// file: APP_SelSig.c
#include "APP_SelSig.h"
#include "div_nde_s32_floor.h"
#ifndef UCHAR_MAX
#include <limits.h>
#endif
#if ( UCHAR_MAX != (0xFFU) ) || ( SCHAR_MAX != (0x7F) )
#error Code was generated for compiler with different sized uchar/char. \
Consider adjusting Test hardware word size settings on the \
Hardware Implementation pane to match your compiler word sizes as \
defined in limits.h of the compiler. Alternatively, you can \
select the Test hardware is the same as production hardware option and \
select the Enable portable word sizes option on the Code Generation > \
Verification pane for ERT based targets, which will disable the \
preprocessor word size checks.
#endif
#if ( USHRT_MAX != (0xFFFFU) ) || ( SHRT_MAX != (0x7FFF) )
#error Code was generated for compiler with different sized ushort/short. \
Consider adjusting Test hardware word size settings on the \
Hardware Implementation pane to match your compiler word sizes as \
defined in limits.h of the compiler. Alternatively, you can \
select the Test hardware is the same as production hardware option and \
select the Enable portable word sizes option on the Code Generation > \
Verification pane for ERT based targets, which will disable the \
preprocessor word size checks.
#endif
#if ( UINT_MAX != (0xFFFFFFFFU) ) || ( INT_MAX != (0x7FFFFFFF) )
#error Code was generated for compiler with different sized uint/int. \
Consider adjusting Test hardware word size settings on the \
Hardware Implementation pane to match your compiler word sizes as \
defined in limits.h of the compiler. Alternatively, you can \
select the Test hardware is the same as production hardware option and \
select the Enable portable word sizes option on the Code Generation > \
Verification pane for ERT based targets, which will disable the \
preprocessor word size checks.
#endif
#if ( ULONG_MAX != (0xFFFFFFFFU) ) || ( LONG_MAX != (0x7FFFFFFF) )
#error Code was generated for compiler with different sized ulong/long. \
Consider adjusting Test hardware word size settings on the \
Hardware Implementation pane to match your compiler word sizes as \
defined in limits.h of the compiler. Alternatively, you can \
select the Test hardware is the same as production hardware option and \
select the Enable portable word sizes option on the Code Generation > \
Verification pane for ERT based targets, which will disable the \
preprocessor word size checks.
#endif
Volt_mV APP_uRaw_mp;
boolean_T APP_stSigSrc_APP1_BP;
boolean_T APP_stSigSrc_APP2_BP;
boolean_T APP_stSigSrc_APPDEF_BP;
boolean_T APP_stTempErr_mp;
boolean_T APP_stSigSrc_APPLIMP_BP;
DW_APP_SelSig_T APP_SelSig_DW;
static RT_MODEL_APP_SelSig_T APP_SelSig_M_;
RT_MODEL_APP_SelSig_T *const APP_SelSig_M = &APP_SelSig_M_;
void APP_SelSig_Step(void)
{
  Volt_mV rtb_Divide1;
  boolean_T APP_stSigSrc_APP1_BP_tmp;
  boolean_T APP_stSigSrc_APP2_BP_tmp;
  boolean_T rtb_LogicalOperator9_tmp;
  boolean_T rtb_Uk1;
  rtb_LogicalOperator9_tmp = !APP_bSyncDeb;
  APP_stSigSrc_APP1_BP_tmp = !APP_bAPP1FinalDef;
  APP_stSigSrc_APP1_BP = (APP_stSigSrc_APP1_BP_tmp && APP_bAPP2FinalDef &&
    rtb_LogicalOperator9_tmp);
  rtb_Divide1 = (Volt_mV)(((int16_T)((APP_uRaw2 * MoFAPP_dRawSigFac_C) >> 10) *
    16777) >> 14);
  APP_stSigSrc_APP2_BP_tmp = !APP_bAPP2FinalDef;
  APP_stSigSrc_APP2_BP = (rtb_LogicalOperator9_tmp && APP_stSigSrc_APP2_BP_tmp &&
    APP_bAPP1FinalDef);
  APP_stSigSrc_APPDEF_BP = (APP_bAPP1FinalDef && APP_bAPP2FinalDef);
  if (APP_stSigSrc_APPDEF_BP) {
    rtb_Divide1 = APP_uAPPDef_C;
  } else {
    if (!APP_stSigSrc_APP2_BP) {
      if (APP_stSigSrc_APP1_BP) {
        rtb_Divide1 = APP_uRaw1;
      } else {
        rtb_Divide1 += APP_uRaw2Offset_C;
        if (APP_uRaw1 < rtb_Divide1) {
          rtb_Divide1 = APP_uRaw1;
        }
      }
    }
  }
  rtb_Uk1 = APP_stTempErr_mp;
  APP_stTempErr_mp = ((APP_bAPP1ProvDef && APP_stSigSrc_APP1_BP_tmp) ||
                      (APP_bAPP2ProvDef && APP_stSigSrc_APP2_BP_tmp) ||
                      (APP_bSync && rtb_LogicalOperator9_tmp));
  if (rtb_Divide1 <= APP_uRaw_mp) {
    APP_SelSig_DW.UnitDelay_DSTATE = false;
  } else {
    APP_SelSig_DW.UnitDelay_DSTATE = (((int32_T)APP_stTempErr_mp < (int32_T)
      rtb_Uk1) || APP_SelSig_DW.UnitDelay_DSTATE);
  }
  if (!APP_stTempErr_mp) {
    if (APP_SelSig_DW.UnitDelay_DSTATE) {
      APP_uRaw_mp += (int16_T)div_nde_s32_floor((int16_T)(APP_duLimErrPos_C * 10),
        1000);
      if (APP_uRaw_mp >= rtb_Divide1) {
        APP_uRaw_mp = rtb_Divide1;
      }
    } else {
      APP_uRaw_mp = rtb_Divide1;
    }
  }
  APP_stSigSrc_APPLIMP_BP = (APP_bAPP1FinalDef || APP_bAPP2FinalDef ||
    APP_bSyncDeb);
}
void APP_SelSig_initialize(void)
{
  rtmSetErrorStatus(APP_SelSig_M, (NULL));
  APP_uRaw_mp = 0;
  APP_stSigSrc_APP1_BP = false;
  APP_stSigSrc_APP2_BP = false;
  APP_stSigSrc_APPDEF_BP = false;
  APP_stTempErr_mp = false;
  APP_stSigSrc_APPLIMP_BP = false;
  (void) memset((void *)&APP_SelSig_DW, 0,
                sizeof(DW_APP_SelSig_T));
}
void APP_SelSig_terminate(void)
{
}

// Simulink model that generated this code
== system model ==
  APP_SelSig_Step : Inport
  APP_bAPP1FinalDef : Inport
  APP_bAPP2FinalDef : Inport
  APP_bSyncDeb : Inport
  APP_bAPP1ProvDef : Inport
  APP_bAPP2ProvDef : Inport
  APP_bSync : Inport
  APP_uRaw2 : Inport
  APP_uRaw1 : Inport
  APP_uRaw_mp : Outport  <- 1: APP_SelSig
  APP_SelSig : Subsystem  <- 1: APP_bAPP1FinalDef, 2: APP_bAPP2FinalDef, 3: APP_bSyncDeb, 4: APP_bAPP1ProvDef, 5: APP_bAPP2ProvDef, 6: APP_bSync, 7: APP_uRaw2, 8: APP_uRaw1, Trigger: APP_SelSig_Step
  APP_stSigSrc_APPDEF_BP : Outport  <- 1: APP_SelSig/2
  APP_stSigSrc_APP1_BP : Outport  <- 1: APP_SelSig/3
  APP_stSigSrc_APP2_BP : Outport  <- 1: APP_SelSig/4
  APP_stSigSrc_APPLIMP_BP : Outport  <- 1: APP_SelSig/5
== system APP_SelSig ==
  Inport#1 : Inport
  Inport#2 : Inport
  Inport#3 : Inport
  Inport#4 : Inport
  Inport#5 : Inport
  Inport#6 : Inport
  Inport#7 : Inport
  Inport#8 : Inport
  TriggerPort#1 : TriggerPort  TriggerType=function-call
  Outport#1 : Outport  <- 1: Switch#1
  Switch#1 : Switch  Criteria=u2 ~= 0  <- 1: Delay#1, 2: Logic#1, 3: Switch#2
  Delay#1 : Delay  DelayLength=1  InitialCondition=0  <- 1: Switch#1
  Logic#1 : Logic  Operator=OR  Inputs=3  <- 1: Logic#2, 2: Logic#3, 3: Logic#4
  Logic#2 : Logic  <- 1: Inport#4, 2: Logic#5
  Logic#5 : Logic  Operator=NOT  <- 1: Inport#1
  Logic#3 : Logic  <- 1: Inport#5, 2: Logic#6
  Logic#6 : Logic  Operator=NOT  <- 1: Inport#2
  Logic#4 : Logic  <- 1: Inport#6, 2: Logic#7
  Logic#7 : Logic  Operator=NOT  <- 1: Inport#3
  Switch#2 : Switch  Criteria=u2 ~= 0  <- 1: MinMax#1, 2: RSFilpFlop#1, 3: Switch#3
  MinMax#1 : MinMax  Inputs=2  <- 1: Sum#1, 2: Switch#3
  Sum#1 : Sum  <- 1: Delay#1, 2: Product#1
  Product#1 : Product  Inputs=**/  <- 1: Constant#1, 2: Constant#2, 3: Constant#3
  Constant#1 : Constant  Value=APP_duLimErrPos_C
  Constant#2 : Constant  Value=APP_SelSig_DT
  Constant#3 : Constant  Value=1000
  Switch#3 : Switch  Criteria=u2 ~= 0  <- 1: Constant#4, 2: Logic#8, 3: Switch#4
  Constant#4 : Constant  Value=APP_uAPPDef_C
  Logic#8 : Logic  <- 1: Inport#1, 2: Inport#2
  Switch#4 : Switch  Criteria=u2 ~= 0  <- 1: Divide1, 2: Logic#9, 3: Switch#5
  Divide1 : Product  Inputs=**  <- 1: Inport#7, 2: Constant#5
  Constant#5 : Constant  Value=MoFAPP_dRawSigFac_C
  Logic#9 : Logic  Inputs=3  <- 1: LogicalOperator9, 2: Logic#10, 3: Inport#1
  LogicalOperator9 : Logic  Operator=NOT  <- 1: Inport#3
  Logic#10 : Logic  Operator=NOT  <- 1: Inport#2
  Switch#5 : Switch  Criteria=u2 ~= 0  <- 1: Inport#8, 2: Logic#11, 3: MinMax#2
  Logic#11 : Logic  Inputs=3  <- 1: Logic#12, 2: Inport#2, 3: LogicalOperator9
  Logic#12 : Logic  Operator=NOT  <- 1: Inport#1
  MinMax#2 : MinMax  Inputs=2  <- 1: Inport#8, 2: Sum#2
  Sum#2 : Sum  <- 1: Divide1, 2: Constant#6
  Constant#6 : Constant  Value=APP_uRaw2Offset_C
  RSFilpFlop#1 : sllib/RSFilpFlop  <- 1: DetectDecrease#1, 2: RelationalOperator#1
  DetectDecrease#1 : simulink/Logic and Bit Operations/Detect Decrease  <- 1: Logic#1
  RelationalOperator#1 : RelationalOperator  Operator=<=  <- 1: Switch#3, 2: Delay#1
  Outport#2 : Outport  <- 1: Logic#8
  Outport#3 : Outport  <- 1: Logic#11
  Outport#4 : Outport  <- 1: Logic#9
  Outport#5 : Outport  <- 1: Logic#13
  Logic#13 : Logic  Operator=OR  Inputs=3  <- 1: Inport#1, 2: Inport#2, 3: Inport#3
